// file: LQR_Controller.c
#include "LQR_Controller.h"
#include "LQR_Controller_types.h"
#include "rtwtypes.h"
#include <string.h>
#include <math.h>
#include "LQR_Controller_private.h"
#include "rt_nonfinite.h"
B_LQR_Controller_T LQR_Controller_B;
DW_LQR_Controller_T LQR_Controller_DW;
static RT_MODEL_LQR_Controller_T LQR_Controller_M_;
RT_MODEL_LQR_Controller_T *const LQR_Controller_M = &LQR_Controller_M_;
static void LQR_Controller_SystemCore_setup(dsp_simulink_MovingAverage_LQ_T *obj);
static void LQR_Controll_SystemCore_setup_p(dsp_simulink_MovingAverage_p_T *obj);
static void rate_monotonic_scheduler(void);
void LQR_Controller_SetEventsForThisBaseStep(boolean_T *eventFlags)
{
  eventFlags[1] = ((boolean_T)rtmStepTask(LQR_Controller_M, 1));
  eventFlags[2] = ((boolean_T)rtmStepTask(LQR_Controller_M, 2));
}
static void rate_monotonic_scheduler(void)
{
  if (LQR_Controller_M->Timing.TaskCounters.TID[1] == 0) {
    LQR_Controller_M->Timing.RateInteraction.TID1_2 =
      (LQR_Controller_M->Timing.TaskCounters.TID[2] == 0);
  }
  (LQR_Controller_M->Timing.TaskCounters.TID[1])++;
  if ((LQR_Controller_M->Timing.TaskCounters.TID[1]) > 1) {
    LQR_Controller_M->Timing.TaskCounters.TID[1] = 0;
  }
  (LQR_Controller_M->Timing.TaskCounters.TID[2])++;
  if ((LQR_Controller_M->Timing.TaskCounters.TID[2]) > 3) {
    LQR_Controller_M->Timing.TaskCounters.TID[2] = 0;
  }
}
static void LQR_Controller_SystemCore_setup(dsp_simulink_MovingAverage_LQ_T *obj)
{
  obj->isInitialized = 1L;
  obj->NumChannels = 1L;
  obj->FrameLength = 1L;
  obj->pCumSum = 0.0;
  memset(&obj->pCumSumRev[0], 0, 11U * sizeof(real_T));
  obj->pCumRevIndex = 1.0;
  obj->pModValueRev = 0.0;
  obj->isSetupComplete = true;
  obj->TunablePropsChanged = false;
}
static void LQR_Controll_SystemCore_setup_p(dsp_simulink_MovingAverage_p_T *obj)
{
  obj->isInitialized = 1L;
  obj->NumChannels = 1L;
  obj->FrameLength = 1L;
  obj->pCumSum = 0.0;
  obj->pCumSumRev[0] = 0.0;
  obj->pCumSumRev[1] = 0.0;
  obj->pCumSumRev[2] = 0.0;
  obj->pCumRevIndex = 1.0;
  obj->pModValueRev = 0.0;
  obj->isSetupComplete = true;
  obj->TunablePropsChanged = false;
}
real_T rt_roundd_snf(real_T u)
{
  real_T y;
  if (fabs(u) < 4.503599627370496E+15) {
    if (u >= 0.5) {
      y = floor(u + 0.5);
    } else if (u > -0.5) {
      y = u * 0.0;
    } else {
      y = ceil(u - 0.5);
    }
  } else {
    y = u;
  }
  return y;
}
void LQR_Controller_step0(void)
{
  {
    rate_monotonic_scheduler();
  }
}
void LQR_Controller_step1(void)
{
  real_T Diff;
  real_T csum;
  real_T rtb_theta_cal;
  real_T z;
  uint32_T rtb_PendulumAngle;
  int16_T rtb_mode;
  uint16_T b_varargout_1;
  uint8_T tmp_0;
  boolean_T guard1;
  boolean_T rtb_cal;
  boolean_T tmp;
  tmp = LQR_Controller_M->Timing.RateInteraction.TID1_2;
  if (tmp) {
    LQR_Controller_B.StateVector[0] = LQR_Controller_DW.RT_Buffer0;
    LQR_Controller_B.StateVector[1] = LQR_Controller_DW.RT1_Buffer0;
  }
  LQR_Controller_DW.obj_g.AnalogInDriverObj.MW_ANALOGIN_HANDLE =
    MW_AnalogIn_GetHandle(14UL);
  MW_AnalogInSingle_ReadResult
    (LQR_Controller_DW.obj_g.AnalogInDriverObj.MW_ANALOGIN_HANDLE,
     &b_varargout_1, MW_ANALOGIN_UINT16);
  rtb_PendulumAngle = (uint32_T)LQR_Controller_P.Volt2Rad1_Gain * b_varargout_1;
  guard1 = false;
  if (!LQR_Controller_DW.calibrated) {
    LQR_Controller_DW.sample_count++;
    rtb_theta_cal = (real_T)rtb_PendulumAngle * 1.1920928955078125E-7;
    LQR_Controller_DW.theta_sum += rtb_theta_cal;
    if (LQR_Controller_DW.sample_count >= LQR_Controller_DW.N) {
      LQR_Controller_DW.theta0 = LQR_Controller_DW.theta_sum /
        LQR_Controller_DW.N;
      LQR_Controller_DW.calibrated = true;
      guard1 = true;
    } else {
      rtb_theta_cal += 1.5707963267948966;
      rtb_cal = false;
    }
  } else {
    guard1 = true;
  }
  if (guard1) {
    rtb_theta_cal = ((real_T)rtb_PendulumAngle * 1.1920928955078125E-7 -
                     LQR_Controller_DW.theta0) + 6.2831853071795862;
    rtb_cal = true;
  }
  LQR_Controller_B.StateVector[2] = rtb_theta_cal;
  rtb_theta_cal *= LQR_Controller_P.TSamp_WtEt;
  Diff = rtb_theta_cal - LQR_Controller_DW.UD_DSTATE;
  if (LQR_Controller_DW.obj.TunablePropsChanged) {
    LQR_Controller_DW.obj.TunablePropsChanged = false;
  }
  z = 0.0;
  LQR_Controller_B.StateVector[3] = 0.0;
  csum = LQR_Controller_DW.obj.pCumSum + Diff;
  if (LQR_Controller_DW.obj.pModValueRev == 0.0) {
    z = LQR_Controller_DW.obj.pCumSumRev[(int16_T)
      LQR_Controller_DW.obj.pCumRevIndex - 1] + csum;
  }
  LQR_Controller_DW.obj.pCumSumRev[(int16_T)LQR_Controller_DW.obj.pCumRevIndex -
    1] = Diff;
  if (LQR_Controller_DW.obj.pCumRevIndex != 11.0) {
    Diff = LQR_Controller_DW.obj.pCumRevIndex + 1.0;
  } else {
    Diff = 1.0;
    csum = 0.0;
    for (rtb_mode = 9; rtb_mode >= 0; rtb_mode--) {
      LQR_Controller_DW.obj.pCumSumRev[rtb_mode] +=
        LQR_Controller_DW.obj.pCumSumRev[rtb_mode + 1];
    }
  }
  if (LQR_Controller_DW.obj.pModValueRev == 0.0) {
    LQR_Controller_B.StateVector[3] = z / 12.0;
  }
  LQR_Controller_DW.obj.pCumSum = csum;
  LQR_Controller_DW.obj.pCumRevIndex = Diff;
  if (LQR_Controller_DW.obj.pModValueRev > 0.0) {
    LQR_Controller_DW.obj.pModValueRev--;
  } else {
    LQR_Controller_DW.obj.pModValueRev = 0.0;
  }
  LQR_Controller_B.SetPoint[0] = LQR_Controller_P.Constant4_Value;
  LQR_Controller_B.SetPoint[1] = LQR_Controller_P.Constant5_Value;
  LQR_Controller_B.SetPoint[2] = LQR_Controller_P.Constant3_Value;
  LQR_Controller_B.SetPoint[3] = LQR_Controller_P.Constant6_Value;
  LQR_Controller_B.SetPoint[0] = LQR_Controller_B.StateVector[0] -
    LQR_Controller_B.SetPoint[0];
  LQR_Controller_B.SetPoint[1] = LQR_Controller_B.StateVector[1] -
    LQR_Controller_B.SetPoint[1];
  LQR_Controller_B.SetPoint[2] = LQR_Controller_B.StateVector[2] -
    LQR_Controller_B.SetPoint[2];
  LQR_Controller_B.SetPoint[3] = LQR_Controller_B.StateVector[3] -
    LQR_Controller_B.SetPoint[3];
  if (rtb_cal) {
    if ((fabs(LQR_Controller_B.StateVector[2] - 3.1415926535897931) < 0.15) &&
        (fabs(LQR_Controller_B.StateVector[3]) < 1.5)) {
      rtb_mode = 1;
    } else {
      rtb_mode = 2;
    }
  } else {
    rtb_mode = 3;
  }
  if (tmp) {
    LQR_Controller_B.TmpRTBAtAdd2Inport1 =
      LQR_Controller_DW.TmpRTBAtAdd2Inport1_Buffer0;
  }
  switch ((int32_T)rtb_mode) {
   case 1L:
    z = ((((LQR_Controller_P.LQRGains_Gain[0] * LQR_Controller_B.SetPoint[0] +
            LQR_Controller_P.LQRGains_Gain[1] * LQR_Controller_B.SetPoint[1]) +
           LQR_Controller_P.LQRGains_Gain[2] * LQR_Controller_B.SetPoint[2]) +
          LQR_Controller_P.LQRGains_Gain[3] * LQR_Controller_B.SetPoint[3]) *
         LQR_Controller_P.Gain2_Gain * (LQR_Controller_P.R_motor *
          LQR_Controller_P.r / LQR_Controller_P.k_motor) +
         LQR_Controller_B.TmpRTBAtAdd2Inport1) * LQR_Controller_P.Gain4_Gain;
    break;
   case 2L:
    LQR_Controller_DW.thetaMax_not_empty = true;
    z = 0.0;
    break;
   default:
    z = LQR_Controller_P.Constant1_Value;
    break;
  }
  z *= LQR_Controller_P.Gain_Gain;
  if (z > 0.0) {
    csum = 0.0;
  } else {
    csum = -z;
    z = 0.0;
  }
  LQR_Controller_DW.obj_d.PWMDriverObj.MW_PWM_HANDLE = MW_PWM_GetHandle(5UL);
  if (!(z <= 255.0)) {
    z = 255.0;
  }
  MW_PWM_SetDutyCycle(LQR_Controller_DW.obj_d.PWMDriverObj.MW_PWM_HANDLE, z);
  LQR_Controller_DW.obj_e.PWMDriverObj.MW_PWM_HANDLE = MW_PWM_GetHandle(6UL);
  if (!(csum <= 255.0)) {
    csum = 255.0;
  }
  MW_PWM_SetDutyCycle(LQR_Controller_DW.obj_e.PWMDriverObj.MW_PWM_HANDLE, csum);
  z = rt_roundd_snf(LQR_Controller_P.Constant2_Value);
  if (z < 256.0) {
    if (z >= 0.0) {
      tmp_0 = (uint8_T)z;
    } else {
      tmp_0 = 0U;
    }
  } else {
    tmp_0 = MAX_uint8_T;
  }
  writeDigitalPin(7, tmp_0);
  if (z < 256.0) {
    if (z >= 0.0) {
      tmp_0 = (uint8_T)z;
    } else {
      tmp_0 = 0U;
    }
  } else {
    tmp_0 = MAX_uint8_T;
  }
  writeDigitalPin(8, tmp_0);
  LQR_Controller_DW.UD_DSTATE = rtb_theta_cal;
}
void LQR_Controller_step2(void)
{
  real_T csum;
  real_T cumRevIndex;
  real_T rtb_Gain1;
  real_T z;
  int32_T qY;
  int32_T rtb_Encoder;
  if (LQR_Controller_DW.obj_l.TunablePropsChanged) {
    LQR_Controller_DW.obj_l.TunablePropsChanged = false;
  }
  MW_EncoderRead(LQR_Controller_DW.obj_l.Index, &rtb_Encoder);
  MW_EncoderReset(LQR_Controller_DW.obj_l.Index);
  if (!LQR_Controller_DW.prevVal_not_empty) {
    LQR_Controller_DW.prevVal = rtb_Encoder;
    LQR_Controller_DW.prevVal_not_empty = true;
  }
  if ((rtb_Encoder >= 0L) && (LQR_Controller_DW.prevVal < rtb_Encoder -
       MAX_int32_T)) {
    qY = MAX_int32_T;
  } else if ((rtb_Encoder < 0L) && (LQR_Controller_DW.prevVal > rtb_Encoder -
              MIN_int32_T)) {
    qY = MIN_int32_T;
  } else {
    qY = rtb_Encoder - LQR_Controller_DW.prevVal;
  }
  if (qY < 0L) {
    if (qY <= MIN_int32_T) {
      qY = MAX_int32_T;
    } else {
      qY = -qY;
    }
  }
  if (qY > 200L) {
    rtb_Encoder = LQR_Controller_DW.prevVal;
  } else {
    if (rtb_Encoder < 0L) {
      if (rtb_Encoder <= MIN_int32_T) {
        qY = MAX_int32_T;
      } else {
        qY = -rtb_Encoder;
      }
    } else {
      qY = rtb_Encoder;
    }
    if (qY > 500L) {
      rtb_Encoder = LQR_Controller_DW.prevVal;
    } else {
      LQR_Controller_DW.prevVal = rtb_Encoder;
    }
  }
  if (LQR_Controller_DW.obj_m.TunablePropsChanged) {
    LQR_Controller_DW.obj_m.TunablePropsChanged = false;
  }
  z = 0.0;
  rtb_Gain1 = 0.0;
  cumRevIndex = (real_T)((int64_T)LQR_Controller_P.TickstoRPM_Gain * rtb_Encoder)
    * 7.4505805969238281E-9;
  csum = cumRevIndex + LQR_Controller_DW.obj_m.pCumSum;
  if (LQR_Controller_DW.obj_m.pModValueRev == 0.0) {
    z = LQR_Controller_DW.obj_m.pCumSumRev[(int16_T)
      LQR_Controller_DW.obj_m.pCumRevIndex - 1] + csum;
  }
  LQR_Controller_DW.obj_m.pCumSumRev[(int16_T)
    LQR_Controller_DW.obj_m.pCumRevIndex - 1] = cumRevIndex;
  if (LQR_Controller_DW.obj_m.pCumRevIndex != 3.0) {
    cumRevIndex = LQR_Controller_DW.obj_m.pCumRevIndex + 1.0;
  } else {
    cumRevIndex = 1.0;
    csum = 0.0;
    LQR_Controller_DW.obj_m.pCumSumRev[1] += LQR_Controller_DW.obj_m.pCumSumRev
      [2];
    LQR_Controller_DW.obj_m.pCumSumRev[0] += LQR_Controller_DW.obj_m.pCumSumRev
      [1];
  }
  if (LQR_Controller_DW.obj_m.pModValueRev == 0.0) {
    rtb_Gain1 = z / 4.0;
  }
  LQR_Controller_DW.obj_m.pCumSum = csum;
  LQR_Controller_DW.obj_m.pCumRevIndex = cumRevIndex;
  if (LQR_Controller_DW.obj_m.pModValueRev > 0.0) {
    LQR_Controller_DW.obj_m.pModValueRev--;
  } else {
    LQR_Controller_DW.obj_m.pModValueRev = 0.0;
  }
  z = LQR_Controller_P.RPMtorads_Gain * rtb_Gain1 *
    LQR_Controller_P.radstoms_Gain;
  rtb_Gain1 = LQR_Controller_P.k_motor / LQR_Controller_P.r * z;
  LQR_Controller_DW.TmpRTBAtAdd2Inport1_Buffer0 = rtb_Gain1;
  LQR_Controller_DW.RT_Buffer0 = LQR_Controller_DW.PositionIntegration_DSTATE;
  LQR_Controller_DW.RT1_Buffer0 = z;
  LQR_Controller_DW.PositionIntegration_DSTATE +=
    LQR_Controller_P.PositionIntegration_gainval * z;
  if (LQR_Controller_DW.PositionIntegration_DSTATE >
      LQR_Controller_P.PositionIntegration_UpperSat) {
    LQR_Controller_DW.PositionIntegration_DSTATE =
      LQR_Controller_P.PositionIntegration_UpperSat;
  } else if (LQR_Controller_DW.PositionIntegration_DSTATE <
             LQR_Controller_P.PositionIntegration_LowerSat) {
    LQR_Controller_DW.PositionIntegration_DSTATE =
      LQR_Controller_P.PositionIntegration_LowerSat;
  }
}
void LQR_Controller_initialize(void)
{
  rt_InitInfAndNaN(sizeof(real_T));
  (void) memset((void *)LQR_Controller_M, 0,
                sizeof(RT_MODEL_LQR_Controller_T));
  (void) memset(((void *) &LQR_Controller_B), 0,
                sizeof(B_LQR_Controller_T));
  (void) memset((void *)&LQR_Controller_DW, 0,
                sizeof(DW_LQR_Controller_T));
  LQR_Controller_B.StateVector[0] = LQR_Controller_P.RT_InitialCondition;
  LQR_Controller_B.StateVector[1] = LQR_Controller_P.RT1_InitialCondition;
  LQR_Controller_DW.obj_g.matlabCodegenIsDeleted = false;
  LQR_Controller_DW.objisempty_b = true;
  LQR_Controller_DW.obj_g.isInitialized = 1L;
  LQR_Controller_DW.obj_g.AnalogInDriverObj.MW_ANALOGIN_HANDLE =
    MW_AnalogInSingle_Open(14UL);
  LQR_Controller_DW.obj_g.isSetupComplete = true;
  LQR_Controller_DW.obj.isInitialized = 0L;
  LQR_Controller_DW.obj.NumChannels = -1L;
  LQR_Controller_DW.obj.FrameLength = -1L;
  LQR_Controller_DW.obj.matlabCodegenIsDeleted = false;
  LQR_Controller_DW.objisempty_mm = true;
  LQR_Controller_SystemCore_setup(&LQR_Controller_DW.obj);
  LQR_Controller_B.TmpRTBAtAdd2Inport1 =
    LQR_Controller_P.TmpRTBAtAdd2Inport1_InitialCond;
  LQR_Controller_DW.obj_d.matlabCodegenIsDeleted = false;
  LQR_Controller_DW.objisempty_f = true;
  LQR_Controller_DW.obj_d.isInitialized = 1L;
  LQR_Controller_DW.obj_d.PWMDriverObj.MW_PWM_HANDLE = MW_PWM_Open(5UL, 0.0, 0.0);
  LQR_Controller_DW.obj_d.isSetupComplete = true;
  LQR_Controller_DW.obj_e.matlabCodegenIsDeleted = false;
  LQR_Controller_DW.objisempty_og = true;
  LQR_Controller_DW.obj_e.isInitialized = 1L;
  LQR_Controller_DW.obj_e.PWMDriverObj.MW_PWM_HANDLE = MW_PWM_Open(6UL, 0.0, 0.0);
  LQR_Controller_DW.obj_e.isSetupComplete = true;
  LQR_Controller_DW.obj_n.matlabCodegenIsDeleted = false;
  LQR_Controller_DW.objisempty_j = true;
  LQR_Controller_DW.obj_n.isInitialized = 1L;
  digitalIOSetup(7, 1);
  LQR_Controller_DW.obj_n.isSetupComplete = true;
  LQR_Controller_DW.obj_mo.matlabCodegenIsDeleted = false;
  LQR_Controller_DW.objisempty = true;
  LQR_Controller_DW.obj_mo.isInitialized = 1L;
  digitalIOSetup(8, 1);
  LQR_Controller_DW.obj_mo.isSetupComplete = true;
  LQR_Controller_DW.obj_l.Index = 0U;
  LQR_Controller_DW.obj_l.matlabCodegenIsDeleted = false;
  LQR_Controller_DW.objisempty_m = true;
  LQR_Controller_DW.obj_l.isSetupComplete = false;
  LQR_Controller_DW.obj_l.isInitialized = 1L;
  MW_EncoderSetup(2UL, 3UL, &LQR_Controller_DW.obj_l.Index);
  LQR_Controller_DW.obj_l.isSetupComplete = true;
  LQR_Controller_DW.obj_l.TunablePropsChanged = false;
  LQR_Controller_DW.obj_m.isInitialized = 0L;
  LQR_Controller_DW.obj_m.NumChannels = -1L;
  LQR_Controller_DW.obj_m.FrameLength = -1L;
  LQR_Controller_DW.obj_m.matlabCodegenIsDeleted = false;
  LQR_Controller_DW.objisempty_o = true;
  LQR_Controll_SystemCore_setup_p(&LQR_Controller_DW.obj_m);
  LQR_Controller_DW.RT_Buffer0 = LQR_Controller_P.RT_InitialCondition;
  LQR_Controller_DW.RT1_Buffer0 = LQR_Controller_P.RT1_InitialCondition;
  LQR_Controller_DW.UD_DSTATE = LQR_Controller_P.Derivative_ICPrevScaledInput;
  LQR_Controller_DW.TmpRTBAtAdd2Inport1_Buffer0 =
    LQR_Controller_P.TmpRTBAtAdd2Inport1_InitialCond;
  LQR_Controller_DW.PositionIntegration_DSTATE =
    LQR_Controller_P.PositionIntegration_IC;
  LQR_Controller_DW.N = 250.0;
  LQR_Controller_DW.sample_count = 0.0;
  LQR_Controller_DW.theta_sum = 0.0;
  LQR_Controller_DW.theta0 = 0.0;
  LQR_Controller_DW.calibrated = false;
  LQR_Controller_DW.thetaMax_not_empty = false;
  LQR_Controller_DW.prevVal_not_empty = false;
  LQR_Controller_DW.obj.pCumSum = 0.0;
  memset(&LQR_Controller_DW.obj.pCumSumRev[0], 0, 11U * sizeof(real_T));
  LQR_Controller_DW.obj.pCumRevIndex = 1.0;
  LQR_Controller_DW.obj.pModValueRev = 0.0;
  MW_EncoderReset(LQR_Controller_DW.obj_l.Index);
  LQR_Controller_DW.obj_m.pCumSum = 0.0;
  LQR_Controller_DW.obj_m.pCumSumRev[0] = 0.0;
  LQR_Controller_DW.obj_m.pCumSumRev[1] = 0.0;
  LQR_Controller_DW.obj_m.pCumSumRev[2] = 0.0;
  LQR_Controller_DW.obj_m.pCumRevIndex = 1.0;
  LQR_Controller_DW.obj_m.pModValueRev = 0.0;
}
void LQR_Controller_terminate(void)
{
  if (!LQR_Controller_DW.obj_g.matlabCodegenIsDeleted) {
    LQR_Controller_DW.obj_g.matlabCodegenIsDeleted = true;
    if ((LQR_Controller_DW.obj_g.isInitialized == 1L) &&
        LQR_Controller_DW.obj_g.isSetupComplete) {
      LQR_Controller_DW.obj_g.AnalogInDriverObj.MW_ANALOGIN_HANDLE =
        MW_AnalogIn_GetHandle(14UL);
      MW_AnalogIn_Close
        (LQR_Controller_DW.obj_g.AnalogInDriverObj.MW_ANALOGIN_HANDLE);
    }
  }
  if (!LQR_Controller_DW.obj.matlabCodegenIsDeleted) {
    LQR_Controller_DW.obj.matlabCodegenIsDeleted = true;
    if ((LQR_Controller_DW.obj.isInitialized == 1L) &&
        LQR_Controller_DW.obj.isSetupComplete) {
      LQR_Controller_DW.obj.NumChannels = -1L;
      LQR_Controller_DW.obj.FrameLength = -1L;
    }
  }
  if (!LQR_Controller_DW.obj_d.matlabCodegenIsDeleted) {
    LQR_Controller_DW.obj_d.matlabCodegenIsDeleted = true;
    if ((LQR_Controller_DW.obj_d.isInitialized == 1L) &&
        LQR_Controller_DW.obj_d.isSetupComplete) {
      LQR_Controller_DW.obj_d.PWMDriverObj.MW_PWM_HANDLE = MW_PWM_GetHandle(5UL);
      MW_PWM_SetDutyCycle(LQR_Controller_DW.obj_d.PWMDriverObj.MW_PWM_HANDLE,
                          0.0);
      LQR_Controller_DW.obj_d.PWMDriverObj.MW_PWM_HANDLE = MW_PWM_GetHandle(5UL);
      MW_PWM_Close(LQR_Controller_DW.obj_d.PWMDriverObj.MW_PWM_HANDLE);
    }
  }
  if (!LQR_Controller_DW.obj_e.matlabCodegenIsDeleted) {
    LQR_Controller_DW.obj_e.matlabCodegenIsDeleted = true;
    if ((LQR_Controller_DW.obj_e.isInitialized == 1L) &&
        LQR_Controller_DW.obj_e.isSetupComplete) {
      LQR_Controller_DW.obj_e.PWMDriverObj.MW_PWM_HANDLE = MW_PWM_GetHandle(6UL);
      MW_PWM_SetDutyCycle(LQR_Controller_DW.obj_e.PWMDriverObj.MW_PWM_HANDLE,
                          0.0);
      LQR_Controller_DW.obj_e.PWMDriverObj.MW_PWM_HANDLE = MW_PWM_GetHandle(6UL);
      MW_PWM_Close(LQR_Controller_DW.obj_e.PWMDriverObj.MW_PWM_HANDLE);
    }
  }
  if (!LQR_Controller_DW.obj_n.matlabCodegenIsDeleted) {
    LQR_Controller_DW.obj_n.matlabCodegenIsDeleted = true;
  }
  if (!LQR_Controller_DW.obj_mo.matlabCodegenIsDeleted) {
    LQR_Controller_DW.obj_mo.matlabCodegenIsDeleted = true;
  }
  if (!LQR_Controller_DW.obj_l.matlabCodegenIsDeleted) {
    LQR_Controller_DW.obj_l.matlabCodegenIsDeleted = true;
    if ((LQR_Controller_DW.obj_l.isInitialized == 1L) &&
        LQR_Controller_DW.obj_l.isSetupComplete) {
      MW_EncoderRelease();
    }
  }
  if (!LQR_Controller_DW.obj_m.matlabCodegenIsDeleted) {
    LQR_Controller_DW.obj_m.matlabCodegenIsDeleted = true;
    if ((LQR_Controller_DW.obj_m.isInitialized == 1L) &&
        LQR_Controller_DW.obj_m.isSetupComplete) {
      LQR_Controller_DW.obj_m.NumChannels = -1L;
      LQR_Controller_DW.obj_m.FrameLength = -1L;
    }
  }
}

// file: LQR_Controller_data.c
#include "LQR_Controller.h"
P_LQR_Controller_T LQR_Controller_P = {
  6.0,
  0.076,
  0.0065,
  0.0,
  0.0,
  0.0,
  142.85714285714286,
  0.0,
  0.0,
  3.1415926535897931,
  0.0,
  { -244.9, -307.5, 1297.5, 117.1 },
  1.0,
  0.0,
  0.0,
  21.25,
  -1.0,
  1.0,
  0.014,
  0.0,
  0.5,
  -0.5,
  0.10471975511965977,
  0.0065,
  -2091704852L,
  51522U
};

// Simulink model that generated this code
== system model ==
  PWM : arduinolib/PWM  pinNumber=5  <- 1: MATLABFunction#1
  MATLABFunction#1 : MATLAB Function  <- 1: Gain
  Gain : Gain  Gain=-1  <- 1: Merge#1
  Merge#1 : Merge  Inputs=3  <- 1: LQR, 2: Subsystem#1, 3: Subsystem#2
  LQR : Subsystem  <- 1: Gain4, Action: SwitchCase#1
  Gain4 : Gain  Gain=255/12  <- 1: Sum#1
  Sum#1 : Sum  <- 1: Gain1, 2: Gain2
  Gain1 : Gain  Gain=k_motor/r  <- 1: radstoms
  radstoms : Gain  Gain=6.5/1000  <- 1: RPMtorads
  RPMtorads : Gain  Gain=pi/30  <- 1: MovingAverage
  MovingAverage : dspstat3/Moving Average  <- 1: DataTypeConversion#1
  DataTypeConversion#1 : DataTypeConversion  <- 1: TickstoRPM
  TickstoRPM : Gain  Gain=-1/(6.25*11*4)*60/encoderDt  <- 1: MATLABFunction#2
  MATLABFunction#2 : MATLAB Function  <- 1: Encoder
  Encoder : arduinosensorlib/Encoder
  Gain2 : Gain  Gain=R_motor*r/k_motor  <- 1: Gain#1
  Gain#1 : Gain  <- 1: LQRGains
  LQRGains : Gain  Gain=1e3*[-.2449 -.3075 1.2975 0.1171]  Multiplication=Matrix(K*u)  <- 1: Sum#2
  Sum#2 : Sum  Inputs=+-  <- 1: StateVector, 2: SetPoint
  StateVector : Concatenate  <- 1: RT, 2: RT1, 3: MATLABFunction#3, 4: MovingAverage#1
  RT : RateTransition  <- 1: PositionIntegration
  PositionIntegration : DiscreteIntegrator  LimitOutput=on  UpperSaturationLimit=.5  LowerSaturationLimit=-.5  <- 1: radstoms
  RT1 : RateTransition  <- 1: radstoms
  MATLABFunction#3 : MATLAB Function  <- 1: DataTypeConversion#2
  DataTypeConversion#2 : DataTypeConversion  <- 1: Volt2Rad1
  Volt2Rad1 : Gain  Gain=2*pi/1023  <- 1: AnalogInput#1
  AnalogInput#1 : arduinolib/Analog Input  pinNumber=0
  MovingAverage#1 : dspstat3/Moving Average  <- 1: Derivative
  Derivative : simulink/Discrete/Discrete Derivative  gainval=1.0  <- 1: MATLABFunction#3
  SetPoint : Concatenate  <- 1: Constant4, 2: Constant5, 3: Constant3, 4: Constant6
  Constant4 : Constant  Value=0
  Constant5 : Constant  Value=0
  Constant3 : Constant  Value=pi
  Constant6 : Constant  Value=0
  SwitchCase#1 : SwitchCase  CaseConditions={1,2}  <- 1: MATLABFunction#4
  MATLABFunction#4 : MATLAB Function  <- 1: StateVector, 2: MATLABFunction#3/2
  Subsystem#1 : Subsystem  <- 1: StateVector, Action: SwitchCase#1/2
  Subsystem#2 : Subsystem  <- 1: Constant1, Action: SwitchCase#1/3
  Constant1 : Constant  Value=0
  PWM#1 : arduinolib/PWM  pinNumber=6  <- 1: MATLABFunction#1/2
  DigitalOutput#1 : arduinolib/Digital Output  pinNumber=7  <- 1: Constant2
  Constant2 : Constant
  DigitalOutput#2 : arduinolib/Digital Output  pinNumber=8  <- 1: Constant2
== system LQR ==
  Inport#1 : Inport
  ActionPort#1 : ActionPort
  Outport#1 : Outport  <- 1: Inport#1
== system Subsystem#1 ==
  Inport#2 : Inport
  ActionPort#2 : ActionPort
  Outport#2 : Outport  <- 1: MATLABFunction#5
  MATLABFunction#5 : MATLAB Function  <- 1: Inport#2
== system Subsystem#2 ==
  Inport#3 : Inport
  ActionPort#3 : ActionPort
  Outport#3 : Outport  <- 1: Inport#3
== matlab function MATLABFunction#1 ==
function [PosPWM, negPWM] = PWMDir(u)
    if u > 0
        PosPWM = u;
        negPWM = 0;
    else
        negPWM = -u;
        PosPWM = 0;
    end
end

== matlab function MATLABFunction#2 ==
function filtered = filterEncoder(currVal)
%#codegen

persistent prevVal

% Initialize on first call
if isempty(prevVal)
    prevVal = currVal;
end

% Dropout detection
threshold = 200;  % Adjust based on your system

if abs(currVal - prevVal) > threshold
    % Bad reading: keep previous good value
    filtered = prevVal;
elseif abs(currVal) > 500
    % this is also a bad reading, nothing should be greater than this
    filtered = prevVal;
else
    % Good reading: update and pass through
    filtered = currVal;
    prevVal = currVal;
end

== matlab function MATLABFunction#4 ==
function mode = ControllerMode(x, calibrated)
% the controller mode selection acts on the state of the pendulum. In the
% standard stable configuration, the controller will center and perform a
% swing up. Once this is achieved, the controller moves into the LQR
% regulator for upright control.
%
% Inputs:
% x - full state vector [4x1]
% voltage - voltage control input [V]
% calibrated - calibration flag boolean

% demux the input state:

pos = x(1);
vel = x(2);
theta = x(3);
omega = x(4);

% if it's calibrated, continue
if calibrated
    % If it is close enough to the vertical position, run the LQR
    if abs(theta-pi) < 0.15 && abs(omega) < 1.5
        mode = 1;        
    else % if it is close enough to the downward position, run the swing up controller
        mode = 2;
    end
else
    mode = 3;
end

end

== matlab function MATLAB Function1 ==
function [theta_cal, cal] = calibrateAngle(theta_raw)
% Calibrates angle by averaging first N samples at startup,
% then subtracting the average offset and adding pi.
%
% Inputs:
%  - theta_raw : current raw angle measurement
%  - reset     : boolean flag to reset calibration (true at startup)
%
% Output:
%  - theta_cal : calibrated angle (aligned so initial avg = pi)

    persistent sample_count theta_sum theta0 calibrated N

    if isempty(calibrated)
        % Initialization on reset
        N = 250;                % number of samples to average
        sample_count = 0;
        theta_sum = 0;
        theta0 = 0;
        calibrated = false;
        cal = false;
    end

    if ~calibrated
        % Accumulate samples for averaging
        sample_count = sample_count + 1;
        theta_sum = theta_sum + theta_raw;
        
        if sample_count >= N
            theta0 = theta_sum / N;  % average offset
            calibrated = true;
            cal = true;
        end
    end

    if calibrated
        % After calibration, subtract offset and add pi
        theta_cal = theta_raw - theta0 + 2*pi;
        cal = true;
    else
        % During calibration phase, output raw angle
        theta_cal = theta_raw + 1/2*pi; 
        cal = false;
    end
end

== matlab function MATLAB Function1 ==
function u = SwingUpController(x)

% demux the input state:
pos = x(1);
vel = x(2);
theta = x(3);
omega = x(4);

persistent thetaMax

if isempty(thetaMax)
    thetaMax = theta;
end

T = 1.1; % period of pendulum
t = 0.05; % acceleration time of pendulum

alphaBest = thetaMax * sin(2*pi/T*t);

u = 0;

end
